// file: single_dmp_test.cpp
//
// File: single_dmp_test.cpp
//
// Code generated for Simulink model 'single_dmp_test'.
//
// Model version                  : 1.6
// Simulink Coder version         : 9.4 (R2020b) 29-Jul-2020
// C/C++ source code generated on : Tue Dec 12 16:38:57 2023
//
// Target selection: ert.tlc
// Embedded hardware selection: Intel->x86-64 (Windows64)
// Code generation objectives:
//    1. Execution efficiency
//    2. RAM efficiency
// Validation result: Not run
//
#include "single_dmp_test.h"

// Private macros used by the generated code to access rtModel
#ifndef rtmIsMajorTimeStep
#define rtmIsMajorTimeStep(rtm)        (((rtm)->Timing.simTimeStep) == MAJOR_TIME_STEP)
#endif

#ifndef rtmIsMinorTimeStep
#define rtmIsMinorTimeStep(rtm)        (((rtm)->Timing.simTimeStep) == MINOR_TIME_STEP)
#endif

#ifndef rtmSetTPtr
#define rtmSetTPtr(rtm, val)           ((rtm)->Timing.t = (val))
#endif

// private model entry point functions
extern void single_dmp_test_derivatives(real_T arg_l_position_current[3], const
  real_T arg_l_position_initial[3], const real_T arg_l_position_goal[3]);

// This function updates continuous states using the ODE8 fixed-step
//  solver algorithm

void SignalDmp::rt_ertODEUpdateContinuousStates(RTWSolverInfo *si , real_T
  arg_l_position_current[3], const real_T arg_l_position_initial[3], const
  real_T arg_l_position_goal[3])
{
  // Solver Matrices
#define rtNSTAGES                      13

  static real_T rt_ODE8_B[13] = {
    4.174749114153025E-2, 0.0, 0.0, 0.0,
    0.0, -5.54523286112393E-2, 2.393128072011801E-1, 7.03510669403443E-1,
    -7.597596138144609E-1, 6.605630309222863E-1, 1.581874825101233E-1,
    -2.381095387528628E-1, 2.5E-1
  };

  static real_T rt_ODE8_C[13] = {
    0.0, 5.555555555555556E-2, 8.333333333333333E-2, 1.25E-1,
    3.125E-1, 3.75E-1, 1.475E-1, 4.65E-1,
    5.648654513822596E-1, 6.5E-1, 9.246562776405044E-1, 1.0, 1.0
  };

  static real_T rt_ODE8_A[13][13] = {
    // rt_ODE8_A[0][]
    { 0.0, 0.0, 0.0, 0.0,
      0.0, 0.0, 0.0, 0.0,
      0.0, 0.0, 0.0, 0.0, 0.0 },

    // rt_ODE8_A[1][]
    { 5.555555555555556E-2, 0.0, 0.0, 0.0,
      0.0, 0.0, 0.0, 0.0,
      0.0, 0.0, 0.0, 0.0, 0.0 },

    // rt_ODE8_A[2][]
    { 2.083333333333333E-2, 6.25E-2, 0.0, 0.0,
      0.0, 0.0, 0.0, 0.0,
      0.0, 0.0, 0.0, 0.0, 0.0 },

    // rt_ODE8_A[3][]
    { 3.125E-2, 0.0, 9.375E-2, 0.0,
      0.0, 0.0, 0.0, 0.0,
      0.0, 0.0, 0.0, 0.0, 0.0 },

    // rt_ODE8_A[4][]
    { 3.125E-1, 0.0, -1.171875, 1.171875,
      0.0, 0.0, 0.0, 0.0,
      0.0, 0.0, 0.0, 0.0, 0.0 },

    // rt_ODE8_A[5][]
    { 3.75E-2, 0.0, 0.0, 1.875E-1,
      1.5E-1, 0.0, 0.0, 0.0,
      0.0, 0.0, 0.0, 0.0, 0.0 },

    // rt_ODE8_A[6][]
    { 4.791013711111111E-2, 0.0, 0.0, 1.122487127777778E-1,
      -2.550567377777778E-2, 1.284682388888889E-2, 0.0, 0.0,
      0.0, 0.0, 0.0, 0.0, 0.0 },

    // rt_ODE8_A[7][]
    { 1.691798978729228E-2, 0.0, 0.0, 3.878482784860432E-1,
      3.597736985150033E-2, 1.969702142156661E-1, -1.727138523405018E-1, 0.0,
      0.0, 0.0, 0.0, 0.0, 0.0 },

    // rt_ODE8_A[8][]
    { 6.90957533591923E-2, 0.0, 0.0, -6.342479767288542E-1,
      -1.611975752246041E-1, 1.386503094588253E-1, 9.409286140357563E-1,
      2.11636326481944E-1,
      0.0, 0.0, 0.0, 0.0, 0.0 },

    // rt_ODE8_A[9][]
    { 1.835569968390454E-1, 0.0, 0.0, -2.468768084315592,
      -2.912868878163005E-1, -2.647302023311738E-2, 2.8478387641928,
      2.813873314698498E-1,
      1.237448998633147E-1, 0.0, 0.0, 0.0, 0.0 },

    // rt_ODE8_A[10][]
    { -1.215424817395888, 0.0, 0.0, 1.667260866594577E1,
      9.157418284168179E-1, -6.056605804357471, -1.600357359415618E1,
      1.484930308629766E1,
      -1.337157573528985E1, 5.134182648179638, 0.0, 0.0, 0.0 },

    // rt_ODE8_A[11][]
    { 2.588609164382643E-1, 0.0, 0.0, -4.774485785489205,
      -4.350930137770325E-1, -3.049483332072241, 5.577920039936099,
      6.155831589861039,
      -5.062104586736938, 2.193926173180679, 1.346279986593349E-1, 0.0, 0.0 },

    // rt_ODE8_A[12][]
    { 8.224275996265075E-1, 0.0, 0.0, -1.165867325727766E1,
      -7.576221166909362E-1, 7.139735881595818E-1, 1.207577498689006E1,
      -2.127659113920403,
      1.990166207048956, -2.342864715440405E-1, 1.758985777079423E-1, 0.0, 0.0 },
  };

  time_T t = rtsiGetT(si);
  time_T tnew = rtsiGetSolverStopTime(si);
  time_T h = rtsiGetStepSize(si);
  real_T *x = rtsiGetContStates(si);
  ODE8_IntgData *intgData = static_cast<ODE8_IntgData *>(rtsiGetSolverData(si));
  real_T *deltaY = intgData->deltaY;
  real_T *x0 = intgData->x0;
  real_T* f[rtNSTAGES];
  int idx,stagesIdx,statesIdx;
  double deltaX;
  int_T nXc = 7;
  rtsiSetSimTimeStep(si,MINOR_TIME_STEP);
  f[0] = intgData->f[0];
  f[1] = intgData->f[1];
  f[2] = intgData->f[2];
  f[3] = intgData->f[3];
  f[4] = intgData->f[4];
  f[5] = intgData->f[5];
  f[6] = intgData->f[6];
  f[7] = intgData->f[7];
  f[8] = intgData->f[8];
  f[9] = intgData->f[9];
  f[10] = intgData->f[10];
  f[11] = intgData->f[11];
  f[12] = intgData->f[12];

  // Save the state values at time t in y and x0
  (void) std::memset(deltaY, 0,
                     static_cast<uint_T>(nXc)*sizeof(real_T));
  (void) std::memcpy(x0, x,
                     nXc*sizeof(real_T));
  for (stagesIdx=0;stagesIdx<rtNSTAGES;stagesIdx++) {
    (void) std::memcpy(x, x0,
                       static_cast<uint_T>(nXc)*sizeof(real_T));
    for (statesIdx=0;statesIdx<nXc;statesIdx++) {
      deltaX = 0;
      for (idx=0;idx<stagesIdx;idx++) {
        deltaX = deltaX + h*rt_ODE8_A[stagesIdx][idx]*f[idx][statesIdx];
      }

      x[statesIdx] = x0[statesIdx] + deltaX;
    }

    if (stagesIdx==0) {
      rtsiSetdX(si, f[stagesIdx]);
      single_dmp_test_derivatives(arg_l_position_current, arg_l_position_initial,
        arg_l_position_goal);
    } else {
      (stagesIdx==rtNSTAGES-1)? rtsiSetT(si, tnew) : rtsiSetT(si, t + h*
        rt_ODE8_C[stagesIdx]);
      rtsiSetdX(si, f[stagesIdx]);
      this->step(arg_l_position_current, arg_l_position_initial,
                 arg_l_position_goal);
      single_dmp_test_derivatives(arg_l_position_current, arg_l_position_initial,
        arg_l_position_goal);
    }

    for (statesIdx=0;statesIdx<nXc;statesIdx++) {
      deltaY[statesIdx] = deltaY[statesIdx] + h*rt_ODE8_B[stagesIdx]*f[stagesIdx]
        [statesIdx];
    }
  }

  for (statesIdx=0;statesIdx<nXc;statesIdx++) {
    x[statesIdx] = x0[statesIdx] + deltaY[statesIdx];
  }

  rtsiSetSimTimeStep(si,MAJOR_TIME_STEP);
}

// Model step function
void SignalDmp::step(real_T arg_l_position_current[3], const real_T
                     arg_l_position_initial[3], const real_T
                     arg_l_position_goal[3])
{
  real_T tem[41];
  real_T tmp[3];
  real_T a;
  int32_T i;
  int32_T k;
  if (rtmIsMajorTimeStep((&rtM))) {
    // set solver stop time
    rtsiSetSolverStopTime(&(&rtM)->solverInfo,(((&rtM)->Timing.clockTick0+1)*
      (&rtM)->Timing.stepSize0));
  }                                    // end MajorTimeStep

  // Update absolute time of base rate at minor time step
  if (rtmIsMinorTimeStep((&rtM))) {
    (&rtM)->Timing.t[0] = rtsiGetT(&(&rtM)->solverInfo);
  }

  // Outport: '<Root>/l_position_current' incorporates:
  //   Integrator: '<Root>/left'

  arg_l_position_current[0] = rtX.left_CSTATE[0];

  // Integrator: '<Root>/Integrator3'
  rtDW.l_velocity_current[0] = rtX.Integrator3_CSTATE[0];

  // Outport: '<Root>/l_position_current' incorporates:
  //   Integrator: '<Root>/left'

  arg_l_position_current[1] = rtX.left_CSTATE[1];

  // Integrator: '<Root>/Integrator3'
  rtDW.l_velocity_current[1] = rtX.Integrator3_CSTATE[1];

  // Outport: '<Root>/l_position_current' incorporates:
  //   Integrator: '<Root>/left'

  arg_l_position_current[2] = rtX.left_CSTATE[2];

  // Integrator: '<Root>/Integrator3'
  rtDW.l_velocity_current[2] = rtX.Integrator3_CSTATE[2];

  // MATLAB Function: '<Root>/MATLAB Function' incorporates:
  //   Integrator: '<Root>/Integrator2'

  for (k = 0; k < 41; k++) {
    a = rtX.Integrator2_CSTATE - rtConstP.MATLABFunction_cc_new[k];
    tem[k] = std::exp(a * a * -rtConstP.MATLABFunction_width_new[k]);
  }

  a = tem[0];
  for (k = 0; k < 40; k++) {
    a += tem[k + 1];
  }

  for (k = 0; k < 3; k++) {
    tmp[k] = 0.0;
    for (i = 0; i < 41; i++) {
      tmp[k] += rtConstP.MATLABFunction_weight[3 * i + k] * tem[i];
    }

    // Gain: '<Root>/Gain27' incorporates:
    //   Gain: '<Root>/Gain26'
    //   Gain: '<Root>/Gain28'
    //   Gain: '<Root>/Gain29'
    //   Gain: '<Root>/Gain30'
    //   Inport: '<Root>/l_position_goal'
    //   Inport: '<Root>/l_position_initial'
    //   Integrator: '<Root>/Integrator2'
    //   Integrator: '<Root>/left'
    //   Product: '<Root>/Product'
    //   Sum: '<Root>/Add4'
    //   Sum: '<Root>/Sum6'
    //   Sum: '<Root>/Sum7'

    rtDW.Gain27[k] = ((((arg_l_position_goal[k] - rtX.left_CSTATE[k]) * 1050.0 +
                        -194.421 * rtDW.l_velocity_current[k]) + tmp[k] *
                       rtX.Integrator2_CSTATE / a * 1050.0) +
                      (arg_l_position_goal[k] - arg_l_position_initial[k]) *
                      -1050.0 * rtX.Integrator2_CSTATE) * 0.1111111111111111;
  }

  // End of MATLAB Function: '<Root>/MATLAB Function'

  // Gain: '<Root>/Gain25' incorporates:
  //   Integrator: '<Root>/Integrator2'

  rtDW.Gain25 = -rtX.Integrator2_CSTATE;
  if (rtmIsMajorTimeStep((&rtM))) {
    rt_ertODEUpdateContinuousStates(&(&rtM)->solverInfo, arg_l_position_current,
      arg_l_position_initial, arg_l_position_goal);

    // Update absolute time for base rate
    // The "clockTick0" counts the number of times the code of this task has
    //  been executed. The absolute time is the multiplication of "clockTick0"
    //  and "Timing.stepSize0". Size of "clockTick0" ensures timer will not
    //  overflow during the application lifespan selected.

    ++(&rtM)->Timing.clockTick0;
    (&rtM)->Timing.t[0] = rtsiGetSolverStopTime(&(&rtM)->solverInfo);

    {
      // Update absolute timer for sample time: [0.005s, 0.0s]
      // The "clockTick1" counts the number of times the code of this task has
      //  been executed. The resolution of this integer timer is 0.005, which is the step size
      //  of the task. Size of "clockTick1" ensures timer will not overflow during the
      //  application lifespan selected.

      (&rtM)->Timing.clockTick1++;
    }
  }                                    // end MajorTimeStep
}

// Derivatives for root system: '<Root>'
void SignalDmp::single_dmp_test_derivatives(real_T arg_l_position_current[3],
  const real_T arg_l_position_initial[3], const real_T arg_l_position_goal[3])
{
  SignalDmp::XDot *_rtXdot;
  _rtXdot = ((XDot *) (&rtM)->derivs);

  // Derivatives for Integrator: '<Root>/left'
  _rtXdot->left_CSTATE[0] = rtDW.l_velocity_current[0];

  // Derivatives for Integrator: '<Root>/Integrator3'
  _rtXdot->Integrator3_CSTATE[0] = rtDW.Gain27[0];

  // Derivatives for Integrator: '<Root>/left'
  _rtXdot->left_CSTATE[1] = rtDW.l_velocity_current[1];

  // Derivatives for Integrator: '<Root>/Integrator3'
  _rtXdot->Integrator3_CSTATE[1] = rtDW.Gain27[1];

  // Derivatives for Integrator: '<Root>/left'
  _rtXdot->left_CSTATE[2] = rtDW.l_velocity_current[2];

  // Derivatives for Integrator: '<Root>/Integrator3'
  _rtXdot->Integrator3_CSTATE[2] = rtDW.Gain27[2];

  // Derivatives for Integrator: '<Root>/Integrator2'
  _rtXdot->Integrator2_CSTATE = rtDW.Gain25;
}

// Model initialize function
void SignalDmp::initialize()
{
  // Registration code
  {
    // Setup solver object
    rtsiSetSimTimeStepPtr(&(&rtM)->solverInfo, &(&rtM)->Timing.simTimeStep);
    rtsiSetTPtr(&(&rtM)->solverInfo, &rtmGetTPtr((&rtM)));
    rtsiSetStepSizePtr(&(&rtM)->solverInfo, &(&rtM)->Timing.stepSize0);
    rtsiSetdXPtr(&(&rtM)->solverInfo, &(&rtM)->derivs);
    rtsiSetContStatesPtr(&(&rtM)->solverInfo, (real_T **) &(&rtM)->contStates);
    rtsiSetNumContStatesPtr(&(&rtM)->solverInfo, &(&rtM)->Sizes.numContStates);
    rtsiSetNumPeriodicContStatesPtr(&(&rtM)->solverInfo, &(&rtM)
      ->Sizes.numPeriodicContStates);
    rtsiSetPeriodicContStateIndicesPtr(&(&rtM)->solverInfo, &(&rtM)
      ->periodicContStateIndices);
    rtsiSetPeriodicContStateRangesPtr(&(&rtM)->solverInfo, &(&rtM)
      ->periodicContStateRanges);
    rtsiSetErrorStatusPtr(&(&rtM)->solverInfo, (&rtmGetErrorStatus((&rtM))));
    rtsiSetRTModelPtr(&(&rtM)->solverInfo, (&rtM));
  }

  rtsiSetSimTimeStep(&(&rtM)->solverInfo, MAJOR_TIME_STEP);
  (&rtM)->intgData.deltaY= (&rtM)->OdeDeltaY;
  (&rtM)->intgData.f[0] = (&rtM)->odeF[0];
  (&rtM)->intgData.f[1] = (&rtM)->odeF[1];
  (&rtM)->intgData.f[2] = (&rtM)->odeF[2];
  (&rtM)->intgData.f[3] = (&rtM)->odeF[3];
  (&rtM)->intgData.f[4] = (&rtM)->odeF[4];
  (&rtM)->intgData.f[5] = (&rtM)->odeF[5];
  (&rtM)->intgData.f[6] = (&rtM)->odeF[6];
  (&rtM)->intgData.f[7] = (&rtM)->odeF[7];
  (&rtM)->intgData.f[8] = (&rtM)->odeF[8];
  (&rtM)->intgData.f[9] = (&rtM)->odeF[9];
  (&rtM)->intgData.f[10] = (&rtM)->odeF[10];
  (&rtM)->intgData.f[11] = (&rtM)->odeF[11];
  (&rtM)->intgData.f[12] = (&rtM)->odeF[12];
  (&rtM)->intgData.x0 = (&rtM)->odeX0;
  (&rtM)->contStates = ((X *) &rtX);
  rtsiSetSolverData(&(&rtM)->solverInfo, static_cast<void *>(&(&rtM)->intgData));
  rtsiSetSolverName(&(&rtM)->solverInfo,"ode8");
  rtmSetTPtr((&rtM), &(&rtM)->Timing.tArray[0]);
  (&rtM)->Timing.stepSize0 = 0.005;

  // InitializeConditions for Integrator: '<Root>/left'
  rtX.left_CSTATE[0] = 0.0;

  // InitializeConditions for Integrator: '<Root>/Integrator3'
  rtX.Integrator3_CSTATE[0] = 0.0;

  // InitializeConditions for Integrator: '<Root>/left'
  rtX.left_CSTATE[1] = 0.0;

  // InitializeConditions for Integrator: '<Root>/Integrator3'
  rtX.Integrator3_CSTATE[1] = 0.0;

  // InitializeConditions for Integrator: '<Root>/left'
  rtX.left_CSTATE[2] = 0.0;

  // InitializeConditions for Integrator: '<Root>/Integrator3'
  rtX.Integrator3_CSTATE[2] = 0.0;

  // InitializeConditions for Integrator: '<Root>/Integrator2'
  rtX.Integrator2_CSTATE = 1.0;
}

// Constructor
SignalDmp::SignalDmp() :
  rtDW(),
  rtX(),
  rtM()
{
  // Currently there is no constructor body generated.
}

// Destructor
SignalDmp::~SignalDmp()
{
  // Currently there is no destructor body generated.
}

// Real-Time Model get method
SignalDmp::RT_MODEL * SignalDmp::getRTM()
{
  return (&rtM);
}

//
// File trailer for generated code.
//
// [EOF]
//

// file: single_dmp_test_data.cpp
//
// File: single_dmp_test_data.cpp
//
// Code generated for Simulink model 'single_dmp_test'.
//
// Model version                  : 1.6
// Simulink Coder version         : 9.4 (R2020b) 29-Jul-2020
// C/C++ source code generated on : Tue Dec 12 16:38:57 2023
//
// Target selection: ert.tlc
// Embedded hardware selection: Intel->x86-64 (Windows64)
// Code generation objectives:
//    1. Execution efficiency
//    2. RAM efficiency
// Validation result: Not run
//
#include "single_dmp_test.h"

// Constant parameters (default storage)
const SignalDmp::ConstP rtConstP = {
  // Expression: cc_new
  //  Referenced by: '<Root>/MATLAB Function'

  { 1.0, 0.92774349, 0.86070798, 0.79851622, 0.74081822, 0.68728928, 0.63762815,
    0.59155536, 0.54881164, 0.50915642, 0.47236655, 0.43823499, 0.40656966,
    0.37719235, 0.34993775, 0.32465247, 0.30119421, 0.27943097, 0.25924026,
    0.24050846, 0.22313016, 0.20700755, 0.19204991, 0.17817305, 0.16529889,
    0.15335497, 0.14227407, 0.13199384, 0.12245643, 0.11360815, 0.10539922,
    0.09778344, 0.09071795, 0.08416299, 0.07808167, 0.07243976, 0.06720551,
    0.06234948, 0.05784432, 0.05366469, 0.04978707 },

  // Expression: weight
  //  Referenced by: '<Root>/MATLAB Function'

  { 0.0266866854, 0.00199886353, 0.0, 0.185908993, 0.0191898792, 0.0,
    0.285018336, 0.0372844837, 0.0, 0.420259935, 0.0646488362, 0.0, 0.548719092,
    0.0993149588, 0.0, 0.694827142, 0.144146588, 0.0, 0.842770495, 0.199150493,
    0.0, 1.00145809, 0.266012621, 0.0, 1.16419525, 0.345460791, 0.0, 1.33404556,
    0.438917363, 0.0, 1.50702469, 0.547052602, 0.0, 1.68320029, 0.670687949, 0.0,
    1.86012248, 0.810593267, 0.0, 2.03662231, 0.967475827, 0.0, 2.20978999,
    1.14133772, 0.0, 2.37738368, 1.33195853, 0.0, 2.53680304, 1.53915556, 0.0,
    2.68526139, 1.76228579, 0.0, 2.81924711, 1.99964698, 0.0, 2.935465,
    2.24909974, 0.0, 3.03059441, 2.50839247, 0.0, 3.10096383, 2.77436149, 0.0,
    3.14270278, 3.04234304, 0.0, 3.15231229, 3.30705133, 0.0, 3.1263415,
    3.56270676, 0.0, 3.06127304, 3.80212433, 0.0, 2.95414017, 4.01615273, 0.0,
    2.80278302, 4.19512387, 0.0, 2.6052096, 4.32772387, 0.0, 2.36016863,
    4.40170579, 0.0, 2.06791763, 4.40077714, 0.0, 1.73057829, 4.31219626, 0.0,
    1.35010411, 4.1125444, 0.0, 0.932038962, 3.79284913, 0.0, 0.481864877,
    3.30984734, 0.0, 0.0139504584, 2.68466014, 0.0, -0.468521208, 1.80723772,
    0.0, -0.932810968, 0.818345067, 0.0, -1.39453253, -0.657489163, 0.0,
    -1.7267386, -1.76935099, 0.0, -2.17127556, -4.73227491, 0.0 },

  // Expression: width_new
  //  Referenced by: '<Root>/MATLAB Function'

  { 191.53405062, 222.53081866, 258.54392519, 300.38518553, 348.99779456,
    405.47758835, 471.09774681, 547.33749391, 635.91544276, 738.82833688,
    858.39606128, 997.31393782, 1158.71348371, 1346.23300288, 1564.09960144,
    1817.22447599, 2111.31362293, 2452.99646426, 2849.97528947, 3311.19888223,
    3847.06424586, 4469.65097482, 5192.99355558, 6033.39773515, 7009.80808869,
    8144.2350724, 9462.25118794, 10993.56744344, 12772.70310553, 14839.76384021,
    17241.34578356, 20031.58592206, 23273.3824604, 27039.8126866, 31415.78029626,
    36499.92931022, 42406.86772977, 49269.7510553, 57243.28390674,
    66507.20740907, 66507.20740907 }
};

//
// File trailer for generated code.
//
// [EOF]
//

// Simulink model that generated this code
simulink model "single_dmp_test"  (R2020b)
settings: Solver=ode8  StartTime=0.0  StopTime=10.0  FixedStep=0.005  RelTol=1e-3
values from neighbouring files (symbols this model uses):
  cc_new = [1 0.92774349 0.86070798 0.79851622 0.74081822 0.68728928 0.63762815 0.59155536 0.54881164 0.50915642 0.47236655 0.43823499 ... (41 elements, 1x41)]    [my_config_1213.mat]    (also in my_config_1219.mat)
  D = [64.807 64.807 64.807]    [my_config_1213.mat]    (also in my_config_1219.mat)
  K = [1050 1050 1050]    [my_config_1213.mat]    (also in my_config_1219.mat; my_config_1224.mat)
  left_0 = [0 0 0]    [my_config_1219.mat]
  tau1 = 3    [my_config_1213.mat]    (also in my_config_1219.mat)
  weight = [0.0266866854 0.00199886353 0 0.185908993 0.0191898792 0 0.285018336 0.0372844837 0 0.420259935 0.0646488362 0 ... (123 elements, 3x41)]    [my_config_1213.mat]    (also in my_config_1219.mat)
  width_new = [191.53405062 222.53081866 258.54392519 300.38518553 348.99779456 405.47758835 471.09774681 547.33749391 635.91544276 738.82833688 858.39606128 997.31393782 ... (41 elements, 1x41)]    [my_config_1213.mat]    (also in my_config_1219.mat)

== system single_dmp_test ==
  note: 目标位置与当前位置
  note: 起始位置
  note: X3*s^2*tau^2
  note: 目标位置
  note: 目标位置与起始位置
  note: -D*tau1*s*X3'
  note: g-x
  note: q
  l_position_initial : Inport  OutDataTypeStr=double  PortDimensions=3
  l_position_goal : Inport  Port=2  OutDataTypeStr=double  PortDimensions=3
  Add4 : Sum  Inputs=++++
  Gain25 : Gain  Gain=-3/tau1
  Gain26 : Gain  Gain=K
  Gain27 : Gain  Gain=1/tau1^2
  Gain28 : Gain  Gain=-D*tau1
  Gain29 : Gain  Gain=K
  Gain30 : Gain  Gain=-K
  Integrator2 : Integrator  InitialCondition=1
  Integrator3 : Integrator
  MATLAB Function : MATLAB Function  TreatAsAtomicUnit=on
  Product : Product
  Sum6 : Sum  Inputs=|-+
  Sum7 : Sum  Inputs=|+-
  left : Integrator  InitialCondition=left_0
  l_position_current : Outport
  wires:
  Add4/1 -> Gain27/1
  Product/1 -> Add4/4  "l_gain4"
  Gain25/1 -> Integrator2/1
  Integrator3/1 -> Gain28/1, left/1  "l_velocity_current"
  Gain27/1 -> Integrator3/1
  Sum7/1 -> Gain30/1
  Gain30/1 -> Product/1
  Integrator2/1 -> Product/2, Gain25/1, MATLAB Function/1(u)  "s"
  MATLAB Function/1(out) -> Gain26/1
  Sum6/1 -> Gain29/1
  l_position_goal/1 -> Sum7/1, Sum6/2  "l_position_goal"
  Gain29/1 -> Add4/2  "l_gain2"
  left/1 -> l_position_current/1, Sum6/1  "l_position_current"
  l_position_initial/1 -> Sum7/2  "l_position_initial"
  Gain26/1 -> Add4/3  "l_gain3"
  Gain28/1 -> Add4/1  "l_gain1"

== matlab function single_dmp_test/MATLAB Function ==
function out = fcn(u, width_new, weight, cc_new)

% if(u>2.5)
%     y=1;
% elseif(u>=0&&u<=2.5)
%     y=0;
% else
%         y=-1;
% end

tem=exp(-width_new.*(u-cc_new).^2)';
y=(weight * tem * u) / sum(tem) ;

out = y;
